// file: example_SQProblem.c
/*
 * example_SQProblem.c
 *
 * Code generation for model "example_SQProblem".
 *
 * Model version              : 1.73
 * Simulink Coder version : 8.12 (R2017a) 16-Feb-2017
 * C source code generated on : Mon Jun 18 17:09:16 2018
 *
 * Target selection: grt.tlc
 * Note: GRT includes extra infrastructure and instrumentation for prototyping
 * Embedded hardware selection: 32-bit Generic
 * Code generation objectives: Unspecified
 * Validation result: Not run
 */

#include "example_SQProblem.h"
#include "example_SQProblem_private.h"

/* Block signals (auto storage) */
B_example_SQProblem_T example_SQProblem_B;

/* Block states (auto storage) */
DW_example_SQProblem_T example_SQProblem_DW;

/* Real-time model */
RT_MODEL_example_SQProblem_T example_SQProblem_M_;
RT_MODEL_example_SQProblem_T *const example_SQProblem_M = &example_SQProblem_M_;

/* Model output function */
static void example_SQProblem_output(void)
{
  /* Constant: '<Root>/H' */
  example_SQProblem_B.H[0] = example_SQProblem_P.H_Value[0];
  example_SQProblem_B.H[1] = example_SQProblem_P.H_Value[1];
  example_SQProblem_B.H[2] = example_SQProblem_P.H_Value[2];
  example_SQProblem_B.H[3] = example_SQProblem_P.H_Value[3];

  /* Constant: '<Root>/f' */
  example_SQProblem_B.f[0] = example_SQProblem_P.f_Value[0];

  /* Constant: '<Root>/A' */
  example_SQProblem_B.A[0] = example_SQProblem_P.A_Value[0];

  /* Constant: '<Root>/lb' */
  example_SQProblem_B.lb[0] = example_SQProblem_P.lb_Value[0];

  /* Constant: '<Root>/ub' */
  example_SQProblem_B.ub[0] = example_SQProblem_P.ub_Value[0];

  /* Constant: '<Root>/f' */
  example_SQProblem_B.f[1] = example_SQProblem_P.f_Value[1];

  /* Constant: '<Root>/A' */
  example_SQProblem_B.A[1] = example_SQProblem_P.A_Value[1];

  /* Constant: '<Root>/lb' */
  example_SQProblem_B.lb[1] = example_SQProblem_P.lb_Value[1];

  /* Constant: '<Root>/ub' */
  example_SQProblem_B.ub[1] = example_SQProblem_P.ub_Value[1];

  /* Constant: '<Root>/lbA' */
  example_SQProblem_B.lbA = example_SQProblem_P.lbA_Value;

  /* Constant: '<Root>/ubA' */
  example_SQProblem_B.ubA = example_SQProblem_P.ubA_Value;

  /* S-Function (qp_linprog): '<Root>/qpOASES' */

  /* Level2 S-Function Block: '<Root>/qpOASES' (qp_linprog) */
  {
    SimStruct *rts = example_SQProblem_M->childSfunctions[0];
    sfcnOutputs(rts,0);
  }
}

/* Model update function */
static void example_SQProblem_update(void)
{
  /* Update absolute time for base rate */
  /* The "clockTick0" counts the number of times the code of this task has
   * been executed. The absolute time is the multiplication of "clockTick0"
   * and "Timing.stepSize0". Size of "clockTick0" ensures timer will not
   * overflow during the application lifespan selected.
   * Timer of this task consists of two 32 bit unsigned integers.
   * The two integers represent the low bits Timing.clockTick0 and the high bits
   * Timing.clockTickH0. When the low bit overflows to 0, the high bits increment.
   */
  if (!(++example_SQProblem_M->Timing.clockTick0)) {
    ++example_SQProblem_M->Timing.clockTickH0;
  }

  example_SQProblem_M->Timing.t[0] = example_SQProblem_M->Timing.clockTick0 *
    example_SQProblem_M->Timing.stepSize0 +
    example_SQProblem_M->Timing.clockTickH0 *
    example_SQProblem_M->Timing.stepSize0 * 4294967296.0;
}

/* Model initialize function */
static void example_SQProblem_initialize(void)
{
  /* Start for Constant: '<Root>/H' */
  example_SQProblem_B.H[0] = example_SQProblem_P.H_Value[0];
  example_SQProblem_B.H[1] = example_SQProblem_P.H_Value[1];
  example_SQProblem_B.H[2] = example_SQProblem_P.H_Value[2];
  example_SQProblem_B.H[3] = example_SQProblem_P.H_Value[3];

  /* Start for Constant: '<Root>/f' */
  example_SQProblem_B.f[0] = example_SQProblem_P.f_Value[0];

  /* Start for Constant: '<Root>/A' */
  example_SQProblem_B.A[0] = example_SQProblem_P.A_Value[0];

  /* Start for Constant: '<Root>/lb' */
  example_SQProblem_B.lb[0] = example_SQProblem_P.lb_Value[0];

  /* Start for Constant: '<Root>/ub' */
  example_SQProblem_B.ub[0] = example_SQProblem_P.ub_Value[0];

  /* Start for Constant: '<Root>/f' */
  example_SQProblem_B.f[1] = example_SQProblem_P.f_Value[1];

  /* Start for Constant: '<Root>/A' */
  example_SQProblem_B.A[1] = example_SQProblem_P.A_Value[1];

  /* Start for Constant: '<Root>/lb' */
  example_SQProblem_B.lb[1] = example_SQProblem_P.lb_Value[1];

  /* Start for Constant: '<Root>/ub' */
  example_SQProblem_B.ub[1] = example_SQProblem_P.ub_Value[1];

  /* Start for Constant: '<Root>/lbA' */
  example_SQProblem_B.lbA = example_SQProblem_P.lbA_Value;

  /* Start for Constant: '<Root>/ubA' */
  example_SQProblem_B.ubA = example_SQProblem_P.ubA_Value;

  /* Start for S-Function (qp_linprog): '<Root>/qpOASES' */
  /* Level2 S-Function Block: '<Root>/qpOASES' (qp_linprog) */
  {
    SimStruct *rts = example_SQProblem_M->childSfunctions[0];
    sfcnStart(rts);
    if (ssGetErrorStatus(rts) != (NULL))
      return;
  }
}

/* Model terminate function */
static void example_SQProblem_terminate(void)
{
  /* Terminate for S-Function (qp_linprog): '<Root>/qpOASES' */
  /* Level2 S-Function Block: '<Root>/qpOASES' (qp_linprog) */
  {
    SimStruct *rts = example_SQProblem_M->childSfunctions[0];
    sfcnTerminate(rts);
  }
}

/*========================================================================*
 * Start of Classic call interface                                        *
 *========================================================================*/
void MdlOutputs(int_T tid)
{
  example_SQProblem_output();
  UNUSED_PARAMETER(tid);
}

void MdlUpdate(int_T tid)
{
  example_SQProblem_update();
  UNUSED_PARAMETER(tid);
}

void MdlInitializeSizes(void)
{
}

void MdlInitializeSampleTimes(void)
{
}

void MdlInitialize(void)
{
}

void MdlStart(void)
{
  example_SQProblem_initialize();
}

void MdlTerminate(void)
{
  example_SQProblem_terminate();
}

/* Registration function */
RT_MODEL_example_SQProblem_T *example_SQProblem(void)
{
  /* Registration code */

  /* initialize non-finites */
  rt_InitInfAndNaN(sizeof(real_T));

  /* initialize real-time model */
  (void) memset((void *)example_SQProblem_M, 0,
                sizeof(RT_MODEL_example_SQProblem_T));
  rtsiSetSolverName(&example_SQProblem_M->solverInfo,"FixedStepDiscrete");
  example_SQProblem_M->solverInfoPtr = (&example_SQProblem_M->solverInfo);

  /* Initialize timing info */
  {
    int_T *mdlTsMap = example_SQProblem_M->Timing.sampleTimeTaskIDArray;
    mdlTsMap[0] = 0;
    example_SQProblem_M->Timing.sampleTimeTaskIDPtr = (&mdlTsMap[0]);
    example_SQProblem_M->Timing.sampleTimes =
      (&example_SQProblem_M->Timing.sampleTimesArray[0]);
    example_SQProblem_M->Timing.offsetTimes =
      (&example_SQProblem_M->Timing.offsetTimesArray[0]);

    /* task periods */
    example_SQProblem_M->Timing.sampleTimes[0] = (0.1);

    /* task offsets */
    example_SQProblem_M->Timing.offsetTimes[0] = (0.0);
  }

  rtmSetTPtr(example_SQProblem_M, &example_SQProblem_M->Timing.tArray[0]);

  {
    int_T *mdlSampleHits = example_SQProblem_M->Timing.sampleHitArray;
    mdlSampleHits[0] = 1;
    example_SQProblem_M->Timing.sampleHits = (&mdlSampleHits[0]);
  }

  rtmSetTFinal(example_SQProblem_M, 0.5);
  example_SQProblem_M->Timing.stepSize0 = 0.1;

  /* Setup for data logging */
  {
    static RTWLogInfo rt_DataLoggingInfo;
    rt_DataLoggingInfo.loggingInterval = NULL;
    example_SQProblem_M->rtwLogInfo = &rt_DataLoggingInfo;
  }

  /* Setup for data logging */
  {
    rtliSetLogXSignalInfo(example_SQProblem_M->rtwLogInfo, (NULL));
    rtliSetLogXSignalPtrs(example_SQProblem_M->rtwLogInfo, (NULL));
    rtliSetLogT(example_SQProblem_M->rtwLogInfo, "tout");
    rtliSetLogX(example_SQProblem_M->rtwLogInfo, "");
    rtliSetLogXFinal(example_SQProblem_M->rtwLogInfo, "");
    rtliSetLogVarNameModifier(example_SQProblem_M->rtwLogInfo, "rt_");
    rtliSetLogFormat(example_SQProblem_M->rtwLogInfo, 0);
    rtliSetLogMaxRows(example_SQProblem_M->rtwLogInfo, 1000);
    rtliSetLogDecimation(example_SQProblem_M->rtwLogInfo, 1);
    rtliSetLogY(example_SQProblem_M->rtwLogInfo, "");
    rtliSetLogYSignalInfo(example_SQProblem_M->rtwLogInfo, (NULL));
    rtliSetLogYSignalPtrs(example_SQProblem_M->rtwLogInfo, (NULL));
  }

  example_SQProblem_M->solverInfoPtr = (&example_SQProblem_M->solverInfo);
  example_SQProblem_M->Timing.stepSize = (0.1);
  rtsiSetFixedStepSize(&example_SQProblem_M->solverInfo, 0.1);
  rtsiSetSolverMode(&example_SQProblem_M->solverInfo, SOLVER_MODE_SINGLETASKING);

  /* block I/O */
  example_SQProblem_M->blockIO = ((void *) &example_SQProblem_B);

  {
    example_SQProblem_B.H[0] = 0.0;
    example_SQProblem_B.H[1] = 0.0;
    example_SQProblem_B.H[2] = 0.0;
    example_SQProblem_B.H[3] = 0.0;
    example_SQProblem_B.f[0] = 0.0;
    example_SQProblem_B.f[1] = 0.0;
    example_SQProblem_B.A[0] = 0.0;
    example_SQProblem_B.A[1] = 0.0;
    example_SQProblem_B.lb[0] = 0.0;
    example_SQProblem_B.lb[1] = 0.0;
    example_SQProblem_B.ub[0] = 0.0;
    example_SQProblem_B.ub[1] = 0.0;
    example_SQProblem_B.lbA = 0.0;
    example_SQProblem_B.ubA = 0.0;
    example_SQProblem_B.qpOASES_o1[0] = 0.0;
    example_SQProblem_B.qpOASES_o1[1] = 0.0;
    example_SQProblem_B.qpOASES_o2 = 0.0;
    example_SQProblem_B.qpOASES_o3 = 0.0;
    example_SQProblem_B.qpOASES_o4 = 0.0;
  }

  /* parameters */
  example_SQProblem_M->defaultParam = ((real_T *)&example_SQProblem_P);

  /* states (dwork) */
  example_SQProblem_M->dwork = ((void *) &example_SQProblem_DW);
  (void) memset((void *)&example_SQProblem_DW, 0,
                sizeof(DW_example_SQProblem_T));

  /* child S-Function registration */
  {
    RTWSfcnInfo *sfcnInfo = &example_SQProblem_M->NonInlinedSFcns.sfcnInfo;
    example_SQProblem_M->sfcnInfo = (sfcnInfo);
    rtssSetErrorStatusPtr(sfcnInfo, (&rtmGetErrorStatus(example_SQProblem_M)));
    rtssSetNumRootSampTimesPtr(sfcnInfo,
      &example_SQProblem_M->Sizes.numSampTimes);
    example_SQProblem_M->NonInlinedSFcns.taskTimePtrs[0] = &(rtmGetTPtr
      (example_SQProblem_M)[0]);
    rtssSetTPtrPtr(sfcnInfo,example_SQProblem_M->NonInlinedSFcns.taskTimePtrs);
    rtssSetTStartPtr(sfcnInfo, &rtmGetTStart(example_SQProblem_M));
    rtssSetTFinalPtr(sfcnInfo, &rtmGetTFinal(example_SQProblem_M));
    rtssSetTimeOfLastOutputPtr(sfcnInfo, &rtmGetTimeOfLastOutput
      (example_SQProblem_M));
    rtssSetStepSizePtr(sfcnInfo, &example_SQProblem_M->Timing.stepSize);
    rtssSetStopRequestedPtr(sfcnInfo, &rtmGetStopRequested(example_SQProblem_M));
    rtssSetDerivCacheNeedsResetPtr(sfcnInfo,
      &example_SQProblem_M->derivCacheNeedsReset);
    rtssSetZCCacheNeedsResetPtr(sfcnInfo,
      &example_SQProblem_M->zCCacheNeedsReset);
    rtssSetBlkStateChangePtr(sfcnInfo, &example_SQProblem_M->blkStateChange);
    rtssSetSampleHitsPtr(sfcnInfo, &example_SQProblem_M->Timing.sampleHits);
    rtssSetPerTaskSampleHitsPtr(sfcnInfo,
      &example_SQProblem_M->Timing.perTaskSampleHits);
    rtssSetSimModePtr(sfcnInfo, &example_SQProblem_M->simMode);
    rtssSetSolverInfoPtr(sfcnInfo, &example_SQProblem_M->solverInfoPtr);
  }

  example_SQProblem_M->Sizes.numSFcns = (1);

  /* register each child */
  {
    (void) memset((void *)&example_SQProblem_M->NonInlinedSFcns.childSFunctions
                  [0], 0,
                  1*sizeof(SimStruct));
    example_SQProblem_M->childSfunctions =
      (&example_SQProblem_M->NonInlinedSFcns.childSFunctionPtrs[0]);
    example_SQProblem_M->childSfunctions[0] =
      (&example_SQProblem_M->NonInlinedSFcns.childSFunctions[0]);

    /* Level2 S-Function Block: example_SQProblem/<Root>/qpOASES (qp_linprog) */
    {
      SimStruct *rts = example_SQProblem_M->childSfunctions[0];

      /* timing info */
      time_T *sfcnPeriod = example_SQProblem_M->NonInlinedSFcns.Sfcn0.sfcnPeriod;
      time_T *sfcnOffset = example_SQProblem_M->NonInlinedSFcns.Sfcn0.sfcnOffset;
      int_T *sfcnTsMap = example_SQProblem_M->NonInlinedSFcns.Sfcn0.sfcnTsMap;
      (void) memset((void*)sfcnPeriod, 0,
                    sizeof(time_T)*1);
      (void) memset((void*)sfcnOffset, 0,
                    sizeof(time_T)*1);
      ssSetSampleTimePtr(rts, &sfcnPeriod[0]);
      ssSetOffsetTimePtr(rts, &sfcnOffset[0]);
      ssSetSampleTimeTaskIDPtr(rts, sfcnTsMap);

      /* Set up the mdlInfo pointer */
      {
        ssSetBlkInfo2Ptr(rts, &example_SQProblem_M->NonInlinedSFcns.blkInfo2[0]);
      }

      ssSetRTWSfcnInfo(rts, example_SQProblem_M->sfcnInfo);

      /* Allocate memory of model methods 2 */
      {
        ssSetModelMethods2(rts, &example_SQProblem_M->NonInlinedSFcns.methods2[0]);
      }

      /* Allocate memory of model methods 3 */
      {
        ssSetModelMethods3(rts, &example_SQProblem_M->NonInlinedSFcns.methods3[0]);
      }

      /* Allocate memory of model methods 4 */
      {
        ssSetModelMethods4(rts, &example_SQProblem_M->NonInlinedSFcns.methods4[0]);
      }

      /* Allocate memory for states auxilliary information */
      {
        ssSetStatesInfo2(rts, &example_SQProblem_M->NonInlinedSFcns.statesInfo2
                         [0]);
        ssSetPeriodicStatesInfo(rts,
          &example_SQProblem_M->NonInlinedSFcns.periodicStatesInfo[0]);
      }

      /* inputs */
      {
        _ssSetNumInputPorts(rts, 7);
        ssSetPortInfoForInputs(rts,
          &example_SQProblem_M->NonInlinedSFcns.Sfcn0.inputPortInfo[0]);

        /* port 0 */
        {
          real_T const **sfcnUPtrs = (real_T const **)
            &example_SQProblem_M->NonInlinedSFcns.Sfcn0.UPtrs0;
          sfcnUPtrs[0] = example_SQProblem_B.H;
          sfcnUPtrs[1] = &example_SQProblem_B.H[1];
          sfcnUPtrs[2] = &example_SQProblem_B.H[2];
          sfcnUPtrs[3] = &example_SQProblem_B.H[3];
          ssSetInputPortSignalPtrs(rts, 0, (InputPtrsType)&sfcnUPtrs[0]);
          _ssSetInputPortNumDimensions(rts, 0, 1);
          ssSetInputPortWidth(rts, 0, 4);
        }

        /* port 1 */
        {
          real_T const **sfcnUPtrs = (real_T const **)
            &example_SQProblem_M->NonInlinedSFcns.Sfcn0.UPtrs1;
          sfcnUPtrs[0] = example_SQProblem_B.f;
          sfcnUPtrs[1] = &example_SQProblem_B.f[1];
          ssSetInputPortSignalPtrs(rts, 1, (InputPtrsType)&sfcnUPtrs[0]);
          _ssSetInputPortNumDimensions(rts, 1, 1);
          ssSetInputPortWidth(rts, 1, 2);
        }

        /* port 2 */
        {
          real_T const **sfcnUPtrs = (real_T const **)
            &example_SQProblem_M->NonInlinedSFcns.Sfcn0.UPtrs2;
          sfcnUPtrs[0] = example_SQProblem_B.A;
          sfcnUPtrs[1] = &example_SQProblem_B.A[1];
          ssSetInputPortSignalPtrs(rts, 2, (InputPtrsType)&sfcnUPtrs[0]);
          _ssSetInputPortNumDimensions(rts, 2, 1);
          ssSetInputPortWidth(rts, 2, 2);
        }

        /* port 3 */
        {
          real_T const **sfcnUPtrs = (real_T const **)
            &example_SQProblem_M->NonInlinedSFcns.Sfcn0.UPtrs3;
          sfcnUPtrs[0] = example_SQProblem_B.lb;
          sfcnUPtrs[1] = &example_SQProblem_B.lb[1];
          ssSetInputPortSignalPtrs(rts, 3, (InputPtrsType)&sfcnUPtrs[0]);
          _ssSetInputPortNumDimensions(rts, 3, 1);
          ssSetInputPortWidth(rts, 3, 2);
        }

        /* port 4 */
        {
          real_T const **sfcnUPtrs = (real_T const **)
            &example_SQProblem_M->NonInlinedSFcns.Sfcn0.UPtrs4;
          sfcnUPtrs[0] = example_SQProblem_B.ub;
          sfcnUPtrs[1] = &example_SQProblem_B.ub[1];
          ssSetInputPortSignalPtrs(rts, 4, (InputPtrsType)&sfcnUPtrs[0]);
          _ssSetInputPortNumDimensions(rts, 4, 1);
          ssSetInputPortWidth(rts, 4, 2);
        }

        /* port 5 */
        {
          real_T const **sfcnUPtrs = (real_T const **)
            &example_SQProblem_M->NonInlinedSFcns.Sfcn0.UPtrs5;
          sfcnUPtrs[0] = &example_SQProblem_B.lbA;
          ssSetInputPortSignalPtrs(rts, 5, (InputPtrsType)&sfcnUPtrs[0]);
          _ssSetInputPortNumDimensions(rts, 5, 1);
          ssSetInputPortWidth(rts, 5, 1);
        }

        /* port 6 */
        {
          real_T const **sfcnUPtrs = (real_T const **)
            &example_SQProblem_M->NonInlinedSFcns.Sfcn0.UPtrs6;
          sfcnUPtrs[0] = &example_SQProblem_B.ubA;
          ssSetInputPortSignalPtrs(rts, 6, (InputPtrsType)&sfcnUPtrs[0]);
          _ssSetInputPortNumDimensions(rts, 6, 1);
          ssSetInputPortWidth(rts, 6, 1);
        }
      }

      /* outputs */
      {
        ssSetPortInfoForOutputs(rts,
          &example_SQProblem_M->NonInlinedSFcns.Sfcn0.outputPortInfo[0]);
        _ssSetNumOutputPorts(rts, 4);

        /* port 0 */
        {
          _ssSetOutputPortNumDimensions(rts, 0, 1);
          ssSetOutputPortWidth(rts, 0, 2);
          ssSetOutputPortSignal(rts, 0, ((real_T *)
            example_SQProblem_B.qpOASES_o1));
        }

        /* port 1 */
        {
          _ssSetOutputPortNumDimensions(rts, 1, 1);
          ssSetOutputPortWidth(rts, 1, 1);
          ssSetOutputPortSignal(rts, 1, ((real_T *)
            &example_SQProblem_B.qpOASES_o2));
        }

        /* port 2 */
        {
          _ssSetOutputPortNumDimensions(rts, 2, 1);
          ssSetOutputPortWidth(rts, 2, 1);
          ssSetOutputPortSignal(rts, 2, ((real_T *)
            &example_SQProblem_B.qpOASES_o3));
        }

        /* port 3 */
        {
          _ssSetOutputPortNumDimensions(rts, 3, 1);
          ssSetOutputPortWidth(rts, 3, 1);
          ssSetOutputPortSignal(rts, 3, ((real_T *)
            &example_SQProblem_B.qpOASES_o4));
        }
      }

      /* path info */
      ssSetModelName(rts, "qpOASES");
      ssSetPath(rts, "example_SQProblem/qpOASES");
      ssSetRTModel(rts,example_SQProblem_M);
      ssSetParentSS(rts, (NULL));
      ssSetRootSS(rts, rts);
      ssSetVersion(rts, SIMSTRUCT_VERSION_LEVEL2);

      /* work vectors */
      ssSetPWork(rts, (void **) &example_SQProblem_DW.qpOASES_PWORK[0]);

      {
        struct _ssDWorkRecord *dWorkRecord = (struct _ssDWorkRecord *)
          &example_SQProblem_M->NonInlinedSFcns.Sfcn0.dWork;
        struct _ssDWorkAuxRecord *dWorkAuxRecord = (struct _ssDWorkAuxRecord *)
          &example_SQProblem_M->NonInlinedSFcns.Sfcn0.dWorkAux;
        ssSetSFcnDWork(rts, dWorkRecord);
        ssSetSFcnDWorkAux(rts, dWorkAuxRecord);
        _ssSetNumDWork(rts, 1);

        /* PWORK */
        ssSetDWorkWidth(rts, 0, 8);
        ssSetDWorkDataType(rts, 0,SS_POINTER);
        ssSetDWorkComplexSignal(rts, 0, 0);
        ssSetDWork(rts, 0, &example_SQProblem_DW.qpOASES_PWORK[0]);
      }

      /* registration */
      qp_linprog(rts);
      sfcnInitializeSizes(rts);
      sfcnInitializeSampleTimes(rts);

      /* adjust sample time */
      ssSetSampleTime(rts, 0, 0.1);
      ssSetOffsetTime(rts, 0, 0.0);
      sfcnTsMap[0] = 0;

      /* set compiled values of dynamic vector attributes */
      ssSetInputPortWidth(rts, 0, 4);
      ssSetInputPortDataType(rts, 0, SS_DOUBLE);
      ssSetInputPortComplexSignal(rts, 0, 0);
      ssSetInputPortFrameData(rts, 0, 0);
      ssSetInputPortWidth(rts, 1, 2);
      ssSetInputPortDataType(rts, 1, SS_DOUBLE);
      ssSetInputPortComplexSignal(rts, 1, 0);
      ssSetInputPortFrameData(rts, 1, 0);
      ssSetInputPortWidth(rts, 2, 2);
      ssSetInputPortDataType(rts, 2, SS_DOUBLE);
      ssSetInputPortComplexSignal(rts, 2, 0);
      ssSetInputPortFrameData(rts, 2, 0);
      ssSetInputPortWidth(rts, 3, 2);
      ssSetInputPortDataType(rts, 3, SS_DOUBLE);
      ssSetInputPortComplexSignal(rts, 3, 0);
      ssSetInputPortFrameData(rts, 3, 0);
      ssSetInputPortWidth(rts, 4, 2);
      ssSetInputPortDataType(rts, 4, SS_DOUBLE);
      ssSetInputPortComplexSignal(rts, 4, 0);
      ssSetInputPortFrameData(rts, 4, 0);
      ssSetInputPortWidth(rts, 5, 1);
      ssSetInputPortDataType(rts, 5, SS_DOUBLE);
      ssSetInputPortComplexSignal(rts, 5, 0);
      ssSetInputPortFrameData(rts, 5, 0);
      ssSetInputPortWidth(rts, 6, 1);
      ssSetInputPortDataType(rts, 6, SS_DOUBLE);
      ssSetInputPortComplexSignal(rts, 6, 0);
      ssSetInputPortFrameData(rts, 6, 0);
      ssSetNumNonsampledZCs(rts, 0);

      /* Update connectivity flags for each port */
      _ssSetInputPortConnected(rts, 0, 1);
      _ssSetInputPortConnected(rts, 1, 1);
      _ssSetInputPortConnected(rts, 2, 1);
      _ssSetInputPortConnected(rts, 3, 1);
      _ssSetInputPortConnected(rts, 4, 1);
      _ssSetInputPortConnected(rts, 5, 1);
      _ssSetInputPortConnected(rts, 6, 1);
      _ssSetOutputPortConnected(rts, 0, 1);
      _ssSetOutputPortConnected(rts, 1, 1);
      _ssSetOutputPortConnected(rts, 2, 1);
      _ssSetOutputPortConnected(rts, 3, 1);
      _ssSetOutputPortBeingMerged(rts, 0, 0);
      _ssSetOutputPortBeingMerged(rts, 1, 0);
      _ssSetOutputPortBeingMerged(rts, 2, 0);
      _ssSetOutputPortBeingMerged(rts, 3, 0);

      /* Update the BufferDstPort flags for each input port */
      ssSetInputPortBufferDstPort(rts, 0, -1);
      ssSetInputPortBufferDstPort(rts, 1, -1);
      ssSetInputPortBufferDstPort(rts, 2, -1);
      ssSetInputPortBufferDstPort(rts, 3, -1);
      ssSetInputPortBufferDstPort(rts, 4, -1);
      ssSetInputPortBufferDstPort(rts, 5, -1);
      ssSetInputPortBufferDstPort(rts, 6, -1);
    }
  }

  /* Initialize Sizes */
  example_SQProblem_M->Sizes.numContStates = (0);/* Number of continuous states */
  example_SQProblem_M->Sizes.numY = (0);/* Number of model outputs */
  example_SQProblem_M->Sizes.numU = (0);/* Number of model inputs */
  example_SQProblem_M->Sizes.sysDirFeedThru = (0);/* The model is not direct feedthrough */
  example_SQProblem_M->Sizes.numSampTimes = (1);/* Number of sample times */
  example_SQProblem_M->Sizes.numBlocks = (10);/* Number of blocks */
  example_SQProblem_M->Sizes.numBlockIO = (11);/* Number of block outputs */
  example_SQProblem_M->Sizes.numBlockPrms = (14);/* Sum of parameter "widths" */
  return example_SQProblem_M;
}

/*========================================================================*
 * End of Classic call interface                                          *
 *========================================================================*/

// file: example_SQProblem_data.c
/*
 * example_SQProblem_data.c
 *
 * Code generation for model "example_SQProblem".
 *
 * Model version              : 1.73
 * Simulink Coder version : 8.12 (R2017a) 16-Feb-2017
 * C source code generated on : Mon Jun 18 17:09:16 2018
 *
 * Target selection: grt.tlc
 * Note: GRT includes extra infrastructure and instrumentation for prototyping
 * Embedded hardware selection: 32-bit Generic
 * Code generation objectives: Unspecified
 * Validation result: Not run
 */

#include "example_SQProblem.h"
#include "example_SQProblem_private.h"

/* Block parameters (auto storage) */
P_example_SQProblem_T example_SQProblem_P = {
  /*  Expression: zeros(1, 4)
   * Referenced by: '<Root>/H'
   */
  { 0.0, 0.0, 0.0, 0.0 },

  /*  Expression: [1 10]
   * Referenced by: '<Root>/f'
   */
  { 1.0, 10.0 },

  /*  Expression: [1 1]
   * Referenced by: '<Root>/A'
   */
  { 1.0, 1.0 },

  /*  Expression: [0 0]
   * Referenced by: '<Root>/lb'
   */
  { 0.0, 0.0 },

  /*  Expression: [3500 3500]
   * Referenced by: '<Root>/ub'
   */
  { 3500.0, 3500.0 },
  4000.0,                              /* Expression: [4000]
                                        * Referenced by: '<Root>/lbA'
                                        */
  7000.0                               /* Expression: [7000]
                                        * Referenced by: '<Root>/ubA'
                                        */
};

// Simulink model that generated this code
simulink model "example_SQProblem"  (Simulink 8.9)
settings: Solver=VariableStepDiscrete  StartTime=0.0  StopTime=0.5  RelTol=1e-3  EnableMultiTasking=on

== system example_SQProblem ==
  note: This file is part of qpOASES.
      |
      | qpOASES -- An Implementation of the Online Active Set Strategy.
      | Copyright (C) 2007-2017 by Hans Joachim Ferreau, Andreas Potschka, Christian Kirches et al.
      | All rights reserved.
  A : Constant  Value=[1 1]
  H : Constant  Value=zeros(1, 4)
  Scope : Scope
  f : Constant  Value=[1 10]
  lb : Constant  Value=[0 0]
  lbA : Constant  Value=[4000]
  qpOASES : S-Function  FunctionName=qp_linprog  SFunctionDeploymentMode=off  EnableBusSupport=off
  ub : Constant  Value=[3500 3500]
  ubA : Constant  Value=[7000]
  "x, fval, exitflag, iter" : Scope  NumInputPorts=4
  wires:
  qpOASES/1 -> Scope/1, "x, fval, exitflag, iter"/1
  qpOASES/2 -> "x, fval, exitflag, iter"/2
  qpOASES/3 -> "x, fval, exitflag, iter"/3
  qpOASES/4 -> "x, fval, exitflag, iter"/4
  H/1 -> qpOASES/1
  f/1 -> qpOASES/2
  A/1 -> qpOASES/3
  lb/1 -> qpOASES/4
  ub/1 -> qpOASES/5
  lbA/1 -> qpOASES/6
  ubA/1 -> qpOASES/7
